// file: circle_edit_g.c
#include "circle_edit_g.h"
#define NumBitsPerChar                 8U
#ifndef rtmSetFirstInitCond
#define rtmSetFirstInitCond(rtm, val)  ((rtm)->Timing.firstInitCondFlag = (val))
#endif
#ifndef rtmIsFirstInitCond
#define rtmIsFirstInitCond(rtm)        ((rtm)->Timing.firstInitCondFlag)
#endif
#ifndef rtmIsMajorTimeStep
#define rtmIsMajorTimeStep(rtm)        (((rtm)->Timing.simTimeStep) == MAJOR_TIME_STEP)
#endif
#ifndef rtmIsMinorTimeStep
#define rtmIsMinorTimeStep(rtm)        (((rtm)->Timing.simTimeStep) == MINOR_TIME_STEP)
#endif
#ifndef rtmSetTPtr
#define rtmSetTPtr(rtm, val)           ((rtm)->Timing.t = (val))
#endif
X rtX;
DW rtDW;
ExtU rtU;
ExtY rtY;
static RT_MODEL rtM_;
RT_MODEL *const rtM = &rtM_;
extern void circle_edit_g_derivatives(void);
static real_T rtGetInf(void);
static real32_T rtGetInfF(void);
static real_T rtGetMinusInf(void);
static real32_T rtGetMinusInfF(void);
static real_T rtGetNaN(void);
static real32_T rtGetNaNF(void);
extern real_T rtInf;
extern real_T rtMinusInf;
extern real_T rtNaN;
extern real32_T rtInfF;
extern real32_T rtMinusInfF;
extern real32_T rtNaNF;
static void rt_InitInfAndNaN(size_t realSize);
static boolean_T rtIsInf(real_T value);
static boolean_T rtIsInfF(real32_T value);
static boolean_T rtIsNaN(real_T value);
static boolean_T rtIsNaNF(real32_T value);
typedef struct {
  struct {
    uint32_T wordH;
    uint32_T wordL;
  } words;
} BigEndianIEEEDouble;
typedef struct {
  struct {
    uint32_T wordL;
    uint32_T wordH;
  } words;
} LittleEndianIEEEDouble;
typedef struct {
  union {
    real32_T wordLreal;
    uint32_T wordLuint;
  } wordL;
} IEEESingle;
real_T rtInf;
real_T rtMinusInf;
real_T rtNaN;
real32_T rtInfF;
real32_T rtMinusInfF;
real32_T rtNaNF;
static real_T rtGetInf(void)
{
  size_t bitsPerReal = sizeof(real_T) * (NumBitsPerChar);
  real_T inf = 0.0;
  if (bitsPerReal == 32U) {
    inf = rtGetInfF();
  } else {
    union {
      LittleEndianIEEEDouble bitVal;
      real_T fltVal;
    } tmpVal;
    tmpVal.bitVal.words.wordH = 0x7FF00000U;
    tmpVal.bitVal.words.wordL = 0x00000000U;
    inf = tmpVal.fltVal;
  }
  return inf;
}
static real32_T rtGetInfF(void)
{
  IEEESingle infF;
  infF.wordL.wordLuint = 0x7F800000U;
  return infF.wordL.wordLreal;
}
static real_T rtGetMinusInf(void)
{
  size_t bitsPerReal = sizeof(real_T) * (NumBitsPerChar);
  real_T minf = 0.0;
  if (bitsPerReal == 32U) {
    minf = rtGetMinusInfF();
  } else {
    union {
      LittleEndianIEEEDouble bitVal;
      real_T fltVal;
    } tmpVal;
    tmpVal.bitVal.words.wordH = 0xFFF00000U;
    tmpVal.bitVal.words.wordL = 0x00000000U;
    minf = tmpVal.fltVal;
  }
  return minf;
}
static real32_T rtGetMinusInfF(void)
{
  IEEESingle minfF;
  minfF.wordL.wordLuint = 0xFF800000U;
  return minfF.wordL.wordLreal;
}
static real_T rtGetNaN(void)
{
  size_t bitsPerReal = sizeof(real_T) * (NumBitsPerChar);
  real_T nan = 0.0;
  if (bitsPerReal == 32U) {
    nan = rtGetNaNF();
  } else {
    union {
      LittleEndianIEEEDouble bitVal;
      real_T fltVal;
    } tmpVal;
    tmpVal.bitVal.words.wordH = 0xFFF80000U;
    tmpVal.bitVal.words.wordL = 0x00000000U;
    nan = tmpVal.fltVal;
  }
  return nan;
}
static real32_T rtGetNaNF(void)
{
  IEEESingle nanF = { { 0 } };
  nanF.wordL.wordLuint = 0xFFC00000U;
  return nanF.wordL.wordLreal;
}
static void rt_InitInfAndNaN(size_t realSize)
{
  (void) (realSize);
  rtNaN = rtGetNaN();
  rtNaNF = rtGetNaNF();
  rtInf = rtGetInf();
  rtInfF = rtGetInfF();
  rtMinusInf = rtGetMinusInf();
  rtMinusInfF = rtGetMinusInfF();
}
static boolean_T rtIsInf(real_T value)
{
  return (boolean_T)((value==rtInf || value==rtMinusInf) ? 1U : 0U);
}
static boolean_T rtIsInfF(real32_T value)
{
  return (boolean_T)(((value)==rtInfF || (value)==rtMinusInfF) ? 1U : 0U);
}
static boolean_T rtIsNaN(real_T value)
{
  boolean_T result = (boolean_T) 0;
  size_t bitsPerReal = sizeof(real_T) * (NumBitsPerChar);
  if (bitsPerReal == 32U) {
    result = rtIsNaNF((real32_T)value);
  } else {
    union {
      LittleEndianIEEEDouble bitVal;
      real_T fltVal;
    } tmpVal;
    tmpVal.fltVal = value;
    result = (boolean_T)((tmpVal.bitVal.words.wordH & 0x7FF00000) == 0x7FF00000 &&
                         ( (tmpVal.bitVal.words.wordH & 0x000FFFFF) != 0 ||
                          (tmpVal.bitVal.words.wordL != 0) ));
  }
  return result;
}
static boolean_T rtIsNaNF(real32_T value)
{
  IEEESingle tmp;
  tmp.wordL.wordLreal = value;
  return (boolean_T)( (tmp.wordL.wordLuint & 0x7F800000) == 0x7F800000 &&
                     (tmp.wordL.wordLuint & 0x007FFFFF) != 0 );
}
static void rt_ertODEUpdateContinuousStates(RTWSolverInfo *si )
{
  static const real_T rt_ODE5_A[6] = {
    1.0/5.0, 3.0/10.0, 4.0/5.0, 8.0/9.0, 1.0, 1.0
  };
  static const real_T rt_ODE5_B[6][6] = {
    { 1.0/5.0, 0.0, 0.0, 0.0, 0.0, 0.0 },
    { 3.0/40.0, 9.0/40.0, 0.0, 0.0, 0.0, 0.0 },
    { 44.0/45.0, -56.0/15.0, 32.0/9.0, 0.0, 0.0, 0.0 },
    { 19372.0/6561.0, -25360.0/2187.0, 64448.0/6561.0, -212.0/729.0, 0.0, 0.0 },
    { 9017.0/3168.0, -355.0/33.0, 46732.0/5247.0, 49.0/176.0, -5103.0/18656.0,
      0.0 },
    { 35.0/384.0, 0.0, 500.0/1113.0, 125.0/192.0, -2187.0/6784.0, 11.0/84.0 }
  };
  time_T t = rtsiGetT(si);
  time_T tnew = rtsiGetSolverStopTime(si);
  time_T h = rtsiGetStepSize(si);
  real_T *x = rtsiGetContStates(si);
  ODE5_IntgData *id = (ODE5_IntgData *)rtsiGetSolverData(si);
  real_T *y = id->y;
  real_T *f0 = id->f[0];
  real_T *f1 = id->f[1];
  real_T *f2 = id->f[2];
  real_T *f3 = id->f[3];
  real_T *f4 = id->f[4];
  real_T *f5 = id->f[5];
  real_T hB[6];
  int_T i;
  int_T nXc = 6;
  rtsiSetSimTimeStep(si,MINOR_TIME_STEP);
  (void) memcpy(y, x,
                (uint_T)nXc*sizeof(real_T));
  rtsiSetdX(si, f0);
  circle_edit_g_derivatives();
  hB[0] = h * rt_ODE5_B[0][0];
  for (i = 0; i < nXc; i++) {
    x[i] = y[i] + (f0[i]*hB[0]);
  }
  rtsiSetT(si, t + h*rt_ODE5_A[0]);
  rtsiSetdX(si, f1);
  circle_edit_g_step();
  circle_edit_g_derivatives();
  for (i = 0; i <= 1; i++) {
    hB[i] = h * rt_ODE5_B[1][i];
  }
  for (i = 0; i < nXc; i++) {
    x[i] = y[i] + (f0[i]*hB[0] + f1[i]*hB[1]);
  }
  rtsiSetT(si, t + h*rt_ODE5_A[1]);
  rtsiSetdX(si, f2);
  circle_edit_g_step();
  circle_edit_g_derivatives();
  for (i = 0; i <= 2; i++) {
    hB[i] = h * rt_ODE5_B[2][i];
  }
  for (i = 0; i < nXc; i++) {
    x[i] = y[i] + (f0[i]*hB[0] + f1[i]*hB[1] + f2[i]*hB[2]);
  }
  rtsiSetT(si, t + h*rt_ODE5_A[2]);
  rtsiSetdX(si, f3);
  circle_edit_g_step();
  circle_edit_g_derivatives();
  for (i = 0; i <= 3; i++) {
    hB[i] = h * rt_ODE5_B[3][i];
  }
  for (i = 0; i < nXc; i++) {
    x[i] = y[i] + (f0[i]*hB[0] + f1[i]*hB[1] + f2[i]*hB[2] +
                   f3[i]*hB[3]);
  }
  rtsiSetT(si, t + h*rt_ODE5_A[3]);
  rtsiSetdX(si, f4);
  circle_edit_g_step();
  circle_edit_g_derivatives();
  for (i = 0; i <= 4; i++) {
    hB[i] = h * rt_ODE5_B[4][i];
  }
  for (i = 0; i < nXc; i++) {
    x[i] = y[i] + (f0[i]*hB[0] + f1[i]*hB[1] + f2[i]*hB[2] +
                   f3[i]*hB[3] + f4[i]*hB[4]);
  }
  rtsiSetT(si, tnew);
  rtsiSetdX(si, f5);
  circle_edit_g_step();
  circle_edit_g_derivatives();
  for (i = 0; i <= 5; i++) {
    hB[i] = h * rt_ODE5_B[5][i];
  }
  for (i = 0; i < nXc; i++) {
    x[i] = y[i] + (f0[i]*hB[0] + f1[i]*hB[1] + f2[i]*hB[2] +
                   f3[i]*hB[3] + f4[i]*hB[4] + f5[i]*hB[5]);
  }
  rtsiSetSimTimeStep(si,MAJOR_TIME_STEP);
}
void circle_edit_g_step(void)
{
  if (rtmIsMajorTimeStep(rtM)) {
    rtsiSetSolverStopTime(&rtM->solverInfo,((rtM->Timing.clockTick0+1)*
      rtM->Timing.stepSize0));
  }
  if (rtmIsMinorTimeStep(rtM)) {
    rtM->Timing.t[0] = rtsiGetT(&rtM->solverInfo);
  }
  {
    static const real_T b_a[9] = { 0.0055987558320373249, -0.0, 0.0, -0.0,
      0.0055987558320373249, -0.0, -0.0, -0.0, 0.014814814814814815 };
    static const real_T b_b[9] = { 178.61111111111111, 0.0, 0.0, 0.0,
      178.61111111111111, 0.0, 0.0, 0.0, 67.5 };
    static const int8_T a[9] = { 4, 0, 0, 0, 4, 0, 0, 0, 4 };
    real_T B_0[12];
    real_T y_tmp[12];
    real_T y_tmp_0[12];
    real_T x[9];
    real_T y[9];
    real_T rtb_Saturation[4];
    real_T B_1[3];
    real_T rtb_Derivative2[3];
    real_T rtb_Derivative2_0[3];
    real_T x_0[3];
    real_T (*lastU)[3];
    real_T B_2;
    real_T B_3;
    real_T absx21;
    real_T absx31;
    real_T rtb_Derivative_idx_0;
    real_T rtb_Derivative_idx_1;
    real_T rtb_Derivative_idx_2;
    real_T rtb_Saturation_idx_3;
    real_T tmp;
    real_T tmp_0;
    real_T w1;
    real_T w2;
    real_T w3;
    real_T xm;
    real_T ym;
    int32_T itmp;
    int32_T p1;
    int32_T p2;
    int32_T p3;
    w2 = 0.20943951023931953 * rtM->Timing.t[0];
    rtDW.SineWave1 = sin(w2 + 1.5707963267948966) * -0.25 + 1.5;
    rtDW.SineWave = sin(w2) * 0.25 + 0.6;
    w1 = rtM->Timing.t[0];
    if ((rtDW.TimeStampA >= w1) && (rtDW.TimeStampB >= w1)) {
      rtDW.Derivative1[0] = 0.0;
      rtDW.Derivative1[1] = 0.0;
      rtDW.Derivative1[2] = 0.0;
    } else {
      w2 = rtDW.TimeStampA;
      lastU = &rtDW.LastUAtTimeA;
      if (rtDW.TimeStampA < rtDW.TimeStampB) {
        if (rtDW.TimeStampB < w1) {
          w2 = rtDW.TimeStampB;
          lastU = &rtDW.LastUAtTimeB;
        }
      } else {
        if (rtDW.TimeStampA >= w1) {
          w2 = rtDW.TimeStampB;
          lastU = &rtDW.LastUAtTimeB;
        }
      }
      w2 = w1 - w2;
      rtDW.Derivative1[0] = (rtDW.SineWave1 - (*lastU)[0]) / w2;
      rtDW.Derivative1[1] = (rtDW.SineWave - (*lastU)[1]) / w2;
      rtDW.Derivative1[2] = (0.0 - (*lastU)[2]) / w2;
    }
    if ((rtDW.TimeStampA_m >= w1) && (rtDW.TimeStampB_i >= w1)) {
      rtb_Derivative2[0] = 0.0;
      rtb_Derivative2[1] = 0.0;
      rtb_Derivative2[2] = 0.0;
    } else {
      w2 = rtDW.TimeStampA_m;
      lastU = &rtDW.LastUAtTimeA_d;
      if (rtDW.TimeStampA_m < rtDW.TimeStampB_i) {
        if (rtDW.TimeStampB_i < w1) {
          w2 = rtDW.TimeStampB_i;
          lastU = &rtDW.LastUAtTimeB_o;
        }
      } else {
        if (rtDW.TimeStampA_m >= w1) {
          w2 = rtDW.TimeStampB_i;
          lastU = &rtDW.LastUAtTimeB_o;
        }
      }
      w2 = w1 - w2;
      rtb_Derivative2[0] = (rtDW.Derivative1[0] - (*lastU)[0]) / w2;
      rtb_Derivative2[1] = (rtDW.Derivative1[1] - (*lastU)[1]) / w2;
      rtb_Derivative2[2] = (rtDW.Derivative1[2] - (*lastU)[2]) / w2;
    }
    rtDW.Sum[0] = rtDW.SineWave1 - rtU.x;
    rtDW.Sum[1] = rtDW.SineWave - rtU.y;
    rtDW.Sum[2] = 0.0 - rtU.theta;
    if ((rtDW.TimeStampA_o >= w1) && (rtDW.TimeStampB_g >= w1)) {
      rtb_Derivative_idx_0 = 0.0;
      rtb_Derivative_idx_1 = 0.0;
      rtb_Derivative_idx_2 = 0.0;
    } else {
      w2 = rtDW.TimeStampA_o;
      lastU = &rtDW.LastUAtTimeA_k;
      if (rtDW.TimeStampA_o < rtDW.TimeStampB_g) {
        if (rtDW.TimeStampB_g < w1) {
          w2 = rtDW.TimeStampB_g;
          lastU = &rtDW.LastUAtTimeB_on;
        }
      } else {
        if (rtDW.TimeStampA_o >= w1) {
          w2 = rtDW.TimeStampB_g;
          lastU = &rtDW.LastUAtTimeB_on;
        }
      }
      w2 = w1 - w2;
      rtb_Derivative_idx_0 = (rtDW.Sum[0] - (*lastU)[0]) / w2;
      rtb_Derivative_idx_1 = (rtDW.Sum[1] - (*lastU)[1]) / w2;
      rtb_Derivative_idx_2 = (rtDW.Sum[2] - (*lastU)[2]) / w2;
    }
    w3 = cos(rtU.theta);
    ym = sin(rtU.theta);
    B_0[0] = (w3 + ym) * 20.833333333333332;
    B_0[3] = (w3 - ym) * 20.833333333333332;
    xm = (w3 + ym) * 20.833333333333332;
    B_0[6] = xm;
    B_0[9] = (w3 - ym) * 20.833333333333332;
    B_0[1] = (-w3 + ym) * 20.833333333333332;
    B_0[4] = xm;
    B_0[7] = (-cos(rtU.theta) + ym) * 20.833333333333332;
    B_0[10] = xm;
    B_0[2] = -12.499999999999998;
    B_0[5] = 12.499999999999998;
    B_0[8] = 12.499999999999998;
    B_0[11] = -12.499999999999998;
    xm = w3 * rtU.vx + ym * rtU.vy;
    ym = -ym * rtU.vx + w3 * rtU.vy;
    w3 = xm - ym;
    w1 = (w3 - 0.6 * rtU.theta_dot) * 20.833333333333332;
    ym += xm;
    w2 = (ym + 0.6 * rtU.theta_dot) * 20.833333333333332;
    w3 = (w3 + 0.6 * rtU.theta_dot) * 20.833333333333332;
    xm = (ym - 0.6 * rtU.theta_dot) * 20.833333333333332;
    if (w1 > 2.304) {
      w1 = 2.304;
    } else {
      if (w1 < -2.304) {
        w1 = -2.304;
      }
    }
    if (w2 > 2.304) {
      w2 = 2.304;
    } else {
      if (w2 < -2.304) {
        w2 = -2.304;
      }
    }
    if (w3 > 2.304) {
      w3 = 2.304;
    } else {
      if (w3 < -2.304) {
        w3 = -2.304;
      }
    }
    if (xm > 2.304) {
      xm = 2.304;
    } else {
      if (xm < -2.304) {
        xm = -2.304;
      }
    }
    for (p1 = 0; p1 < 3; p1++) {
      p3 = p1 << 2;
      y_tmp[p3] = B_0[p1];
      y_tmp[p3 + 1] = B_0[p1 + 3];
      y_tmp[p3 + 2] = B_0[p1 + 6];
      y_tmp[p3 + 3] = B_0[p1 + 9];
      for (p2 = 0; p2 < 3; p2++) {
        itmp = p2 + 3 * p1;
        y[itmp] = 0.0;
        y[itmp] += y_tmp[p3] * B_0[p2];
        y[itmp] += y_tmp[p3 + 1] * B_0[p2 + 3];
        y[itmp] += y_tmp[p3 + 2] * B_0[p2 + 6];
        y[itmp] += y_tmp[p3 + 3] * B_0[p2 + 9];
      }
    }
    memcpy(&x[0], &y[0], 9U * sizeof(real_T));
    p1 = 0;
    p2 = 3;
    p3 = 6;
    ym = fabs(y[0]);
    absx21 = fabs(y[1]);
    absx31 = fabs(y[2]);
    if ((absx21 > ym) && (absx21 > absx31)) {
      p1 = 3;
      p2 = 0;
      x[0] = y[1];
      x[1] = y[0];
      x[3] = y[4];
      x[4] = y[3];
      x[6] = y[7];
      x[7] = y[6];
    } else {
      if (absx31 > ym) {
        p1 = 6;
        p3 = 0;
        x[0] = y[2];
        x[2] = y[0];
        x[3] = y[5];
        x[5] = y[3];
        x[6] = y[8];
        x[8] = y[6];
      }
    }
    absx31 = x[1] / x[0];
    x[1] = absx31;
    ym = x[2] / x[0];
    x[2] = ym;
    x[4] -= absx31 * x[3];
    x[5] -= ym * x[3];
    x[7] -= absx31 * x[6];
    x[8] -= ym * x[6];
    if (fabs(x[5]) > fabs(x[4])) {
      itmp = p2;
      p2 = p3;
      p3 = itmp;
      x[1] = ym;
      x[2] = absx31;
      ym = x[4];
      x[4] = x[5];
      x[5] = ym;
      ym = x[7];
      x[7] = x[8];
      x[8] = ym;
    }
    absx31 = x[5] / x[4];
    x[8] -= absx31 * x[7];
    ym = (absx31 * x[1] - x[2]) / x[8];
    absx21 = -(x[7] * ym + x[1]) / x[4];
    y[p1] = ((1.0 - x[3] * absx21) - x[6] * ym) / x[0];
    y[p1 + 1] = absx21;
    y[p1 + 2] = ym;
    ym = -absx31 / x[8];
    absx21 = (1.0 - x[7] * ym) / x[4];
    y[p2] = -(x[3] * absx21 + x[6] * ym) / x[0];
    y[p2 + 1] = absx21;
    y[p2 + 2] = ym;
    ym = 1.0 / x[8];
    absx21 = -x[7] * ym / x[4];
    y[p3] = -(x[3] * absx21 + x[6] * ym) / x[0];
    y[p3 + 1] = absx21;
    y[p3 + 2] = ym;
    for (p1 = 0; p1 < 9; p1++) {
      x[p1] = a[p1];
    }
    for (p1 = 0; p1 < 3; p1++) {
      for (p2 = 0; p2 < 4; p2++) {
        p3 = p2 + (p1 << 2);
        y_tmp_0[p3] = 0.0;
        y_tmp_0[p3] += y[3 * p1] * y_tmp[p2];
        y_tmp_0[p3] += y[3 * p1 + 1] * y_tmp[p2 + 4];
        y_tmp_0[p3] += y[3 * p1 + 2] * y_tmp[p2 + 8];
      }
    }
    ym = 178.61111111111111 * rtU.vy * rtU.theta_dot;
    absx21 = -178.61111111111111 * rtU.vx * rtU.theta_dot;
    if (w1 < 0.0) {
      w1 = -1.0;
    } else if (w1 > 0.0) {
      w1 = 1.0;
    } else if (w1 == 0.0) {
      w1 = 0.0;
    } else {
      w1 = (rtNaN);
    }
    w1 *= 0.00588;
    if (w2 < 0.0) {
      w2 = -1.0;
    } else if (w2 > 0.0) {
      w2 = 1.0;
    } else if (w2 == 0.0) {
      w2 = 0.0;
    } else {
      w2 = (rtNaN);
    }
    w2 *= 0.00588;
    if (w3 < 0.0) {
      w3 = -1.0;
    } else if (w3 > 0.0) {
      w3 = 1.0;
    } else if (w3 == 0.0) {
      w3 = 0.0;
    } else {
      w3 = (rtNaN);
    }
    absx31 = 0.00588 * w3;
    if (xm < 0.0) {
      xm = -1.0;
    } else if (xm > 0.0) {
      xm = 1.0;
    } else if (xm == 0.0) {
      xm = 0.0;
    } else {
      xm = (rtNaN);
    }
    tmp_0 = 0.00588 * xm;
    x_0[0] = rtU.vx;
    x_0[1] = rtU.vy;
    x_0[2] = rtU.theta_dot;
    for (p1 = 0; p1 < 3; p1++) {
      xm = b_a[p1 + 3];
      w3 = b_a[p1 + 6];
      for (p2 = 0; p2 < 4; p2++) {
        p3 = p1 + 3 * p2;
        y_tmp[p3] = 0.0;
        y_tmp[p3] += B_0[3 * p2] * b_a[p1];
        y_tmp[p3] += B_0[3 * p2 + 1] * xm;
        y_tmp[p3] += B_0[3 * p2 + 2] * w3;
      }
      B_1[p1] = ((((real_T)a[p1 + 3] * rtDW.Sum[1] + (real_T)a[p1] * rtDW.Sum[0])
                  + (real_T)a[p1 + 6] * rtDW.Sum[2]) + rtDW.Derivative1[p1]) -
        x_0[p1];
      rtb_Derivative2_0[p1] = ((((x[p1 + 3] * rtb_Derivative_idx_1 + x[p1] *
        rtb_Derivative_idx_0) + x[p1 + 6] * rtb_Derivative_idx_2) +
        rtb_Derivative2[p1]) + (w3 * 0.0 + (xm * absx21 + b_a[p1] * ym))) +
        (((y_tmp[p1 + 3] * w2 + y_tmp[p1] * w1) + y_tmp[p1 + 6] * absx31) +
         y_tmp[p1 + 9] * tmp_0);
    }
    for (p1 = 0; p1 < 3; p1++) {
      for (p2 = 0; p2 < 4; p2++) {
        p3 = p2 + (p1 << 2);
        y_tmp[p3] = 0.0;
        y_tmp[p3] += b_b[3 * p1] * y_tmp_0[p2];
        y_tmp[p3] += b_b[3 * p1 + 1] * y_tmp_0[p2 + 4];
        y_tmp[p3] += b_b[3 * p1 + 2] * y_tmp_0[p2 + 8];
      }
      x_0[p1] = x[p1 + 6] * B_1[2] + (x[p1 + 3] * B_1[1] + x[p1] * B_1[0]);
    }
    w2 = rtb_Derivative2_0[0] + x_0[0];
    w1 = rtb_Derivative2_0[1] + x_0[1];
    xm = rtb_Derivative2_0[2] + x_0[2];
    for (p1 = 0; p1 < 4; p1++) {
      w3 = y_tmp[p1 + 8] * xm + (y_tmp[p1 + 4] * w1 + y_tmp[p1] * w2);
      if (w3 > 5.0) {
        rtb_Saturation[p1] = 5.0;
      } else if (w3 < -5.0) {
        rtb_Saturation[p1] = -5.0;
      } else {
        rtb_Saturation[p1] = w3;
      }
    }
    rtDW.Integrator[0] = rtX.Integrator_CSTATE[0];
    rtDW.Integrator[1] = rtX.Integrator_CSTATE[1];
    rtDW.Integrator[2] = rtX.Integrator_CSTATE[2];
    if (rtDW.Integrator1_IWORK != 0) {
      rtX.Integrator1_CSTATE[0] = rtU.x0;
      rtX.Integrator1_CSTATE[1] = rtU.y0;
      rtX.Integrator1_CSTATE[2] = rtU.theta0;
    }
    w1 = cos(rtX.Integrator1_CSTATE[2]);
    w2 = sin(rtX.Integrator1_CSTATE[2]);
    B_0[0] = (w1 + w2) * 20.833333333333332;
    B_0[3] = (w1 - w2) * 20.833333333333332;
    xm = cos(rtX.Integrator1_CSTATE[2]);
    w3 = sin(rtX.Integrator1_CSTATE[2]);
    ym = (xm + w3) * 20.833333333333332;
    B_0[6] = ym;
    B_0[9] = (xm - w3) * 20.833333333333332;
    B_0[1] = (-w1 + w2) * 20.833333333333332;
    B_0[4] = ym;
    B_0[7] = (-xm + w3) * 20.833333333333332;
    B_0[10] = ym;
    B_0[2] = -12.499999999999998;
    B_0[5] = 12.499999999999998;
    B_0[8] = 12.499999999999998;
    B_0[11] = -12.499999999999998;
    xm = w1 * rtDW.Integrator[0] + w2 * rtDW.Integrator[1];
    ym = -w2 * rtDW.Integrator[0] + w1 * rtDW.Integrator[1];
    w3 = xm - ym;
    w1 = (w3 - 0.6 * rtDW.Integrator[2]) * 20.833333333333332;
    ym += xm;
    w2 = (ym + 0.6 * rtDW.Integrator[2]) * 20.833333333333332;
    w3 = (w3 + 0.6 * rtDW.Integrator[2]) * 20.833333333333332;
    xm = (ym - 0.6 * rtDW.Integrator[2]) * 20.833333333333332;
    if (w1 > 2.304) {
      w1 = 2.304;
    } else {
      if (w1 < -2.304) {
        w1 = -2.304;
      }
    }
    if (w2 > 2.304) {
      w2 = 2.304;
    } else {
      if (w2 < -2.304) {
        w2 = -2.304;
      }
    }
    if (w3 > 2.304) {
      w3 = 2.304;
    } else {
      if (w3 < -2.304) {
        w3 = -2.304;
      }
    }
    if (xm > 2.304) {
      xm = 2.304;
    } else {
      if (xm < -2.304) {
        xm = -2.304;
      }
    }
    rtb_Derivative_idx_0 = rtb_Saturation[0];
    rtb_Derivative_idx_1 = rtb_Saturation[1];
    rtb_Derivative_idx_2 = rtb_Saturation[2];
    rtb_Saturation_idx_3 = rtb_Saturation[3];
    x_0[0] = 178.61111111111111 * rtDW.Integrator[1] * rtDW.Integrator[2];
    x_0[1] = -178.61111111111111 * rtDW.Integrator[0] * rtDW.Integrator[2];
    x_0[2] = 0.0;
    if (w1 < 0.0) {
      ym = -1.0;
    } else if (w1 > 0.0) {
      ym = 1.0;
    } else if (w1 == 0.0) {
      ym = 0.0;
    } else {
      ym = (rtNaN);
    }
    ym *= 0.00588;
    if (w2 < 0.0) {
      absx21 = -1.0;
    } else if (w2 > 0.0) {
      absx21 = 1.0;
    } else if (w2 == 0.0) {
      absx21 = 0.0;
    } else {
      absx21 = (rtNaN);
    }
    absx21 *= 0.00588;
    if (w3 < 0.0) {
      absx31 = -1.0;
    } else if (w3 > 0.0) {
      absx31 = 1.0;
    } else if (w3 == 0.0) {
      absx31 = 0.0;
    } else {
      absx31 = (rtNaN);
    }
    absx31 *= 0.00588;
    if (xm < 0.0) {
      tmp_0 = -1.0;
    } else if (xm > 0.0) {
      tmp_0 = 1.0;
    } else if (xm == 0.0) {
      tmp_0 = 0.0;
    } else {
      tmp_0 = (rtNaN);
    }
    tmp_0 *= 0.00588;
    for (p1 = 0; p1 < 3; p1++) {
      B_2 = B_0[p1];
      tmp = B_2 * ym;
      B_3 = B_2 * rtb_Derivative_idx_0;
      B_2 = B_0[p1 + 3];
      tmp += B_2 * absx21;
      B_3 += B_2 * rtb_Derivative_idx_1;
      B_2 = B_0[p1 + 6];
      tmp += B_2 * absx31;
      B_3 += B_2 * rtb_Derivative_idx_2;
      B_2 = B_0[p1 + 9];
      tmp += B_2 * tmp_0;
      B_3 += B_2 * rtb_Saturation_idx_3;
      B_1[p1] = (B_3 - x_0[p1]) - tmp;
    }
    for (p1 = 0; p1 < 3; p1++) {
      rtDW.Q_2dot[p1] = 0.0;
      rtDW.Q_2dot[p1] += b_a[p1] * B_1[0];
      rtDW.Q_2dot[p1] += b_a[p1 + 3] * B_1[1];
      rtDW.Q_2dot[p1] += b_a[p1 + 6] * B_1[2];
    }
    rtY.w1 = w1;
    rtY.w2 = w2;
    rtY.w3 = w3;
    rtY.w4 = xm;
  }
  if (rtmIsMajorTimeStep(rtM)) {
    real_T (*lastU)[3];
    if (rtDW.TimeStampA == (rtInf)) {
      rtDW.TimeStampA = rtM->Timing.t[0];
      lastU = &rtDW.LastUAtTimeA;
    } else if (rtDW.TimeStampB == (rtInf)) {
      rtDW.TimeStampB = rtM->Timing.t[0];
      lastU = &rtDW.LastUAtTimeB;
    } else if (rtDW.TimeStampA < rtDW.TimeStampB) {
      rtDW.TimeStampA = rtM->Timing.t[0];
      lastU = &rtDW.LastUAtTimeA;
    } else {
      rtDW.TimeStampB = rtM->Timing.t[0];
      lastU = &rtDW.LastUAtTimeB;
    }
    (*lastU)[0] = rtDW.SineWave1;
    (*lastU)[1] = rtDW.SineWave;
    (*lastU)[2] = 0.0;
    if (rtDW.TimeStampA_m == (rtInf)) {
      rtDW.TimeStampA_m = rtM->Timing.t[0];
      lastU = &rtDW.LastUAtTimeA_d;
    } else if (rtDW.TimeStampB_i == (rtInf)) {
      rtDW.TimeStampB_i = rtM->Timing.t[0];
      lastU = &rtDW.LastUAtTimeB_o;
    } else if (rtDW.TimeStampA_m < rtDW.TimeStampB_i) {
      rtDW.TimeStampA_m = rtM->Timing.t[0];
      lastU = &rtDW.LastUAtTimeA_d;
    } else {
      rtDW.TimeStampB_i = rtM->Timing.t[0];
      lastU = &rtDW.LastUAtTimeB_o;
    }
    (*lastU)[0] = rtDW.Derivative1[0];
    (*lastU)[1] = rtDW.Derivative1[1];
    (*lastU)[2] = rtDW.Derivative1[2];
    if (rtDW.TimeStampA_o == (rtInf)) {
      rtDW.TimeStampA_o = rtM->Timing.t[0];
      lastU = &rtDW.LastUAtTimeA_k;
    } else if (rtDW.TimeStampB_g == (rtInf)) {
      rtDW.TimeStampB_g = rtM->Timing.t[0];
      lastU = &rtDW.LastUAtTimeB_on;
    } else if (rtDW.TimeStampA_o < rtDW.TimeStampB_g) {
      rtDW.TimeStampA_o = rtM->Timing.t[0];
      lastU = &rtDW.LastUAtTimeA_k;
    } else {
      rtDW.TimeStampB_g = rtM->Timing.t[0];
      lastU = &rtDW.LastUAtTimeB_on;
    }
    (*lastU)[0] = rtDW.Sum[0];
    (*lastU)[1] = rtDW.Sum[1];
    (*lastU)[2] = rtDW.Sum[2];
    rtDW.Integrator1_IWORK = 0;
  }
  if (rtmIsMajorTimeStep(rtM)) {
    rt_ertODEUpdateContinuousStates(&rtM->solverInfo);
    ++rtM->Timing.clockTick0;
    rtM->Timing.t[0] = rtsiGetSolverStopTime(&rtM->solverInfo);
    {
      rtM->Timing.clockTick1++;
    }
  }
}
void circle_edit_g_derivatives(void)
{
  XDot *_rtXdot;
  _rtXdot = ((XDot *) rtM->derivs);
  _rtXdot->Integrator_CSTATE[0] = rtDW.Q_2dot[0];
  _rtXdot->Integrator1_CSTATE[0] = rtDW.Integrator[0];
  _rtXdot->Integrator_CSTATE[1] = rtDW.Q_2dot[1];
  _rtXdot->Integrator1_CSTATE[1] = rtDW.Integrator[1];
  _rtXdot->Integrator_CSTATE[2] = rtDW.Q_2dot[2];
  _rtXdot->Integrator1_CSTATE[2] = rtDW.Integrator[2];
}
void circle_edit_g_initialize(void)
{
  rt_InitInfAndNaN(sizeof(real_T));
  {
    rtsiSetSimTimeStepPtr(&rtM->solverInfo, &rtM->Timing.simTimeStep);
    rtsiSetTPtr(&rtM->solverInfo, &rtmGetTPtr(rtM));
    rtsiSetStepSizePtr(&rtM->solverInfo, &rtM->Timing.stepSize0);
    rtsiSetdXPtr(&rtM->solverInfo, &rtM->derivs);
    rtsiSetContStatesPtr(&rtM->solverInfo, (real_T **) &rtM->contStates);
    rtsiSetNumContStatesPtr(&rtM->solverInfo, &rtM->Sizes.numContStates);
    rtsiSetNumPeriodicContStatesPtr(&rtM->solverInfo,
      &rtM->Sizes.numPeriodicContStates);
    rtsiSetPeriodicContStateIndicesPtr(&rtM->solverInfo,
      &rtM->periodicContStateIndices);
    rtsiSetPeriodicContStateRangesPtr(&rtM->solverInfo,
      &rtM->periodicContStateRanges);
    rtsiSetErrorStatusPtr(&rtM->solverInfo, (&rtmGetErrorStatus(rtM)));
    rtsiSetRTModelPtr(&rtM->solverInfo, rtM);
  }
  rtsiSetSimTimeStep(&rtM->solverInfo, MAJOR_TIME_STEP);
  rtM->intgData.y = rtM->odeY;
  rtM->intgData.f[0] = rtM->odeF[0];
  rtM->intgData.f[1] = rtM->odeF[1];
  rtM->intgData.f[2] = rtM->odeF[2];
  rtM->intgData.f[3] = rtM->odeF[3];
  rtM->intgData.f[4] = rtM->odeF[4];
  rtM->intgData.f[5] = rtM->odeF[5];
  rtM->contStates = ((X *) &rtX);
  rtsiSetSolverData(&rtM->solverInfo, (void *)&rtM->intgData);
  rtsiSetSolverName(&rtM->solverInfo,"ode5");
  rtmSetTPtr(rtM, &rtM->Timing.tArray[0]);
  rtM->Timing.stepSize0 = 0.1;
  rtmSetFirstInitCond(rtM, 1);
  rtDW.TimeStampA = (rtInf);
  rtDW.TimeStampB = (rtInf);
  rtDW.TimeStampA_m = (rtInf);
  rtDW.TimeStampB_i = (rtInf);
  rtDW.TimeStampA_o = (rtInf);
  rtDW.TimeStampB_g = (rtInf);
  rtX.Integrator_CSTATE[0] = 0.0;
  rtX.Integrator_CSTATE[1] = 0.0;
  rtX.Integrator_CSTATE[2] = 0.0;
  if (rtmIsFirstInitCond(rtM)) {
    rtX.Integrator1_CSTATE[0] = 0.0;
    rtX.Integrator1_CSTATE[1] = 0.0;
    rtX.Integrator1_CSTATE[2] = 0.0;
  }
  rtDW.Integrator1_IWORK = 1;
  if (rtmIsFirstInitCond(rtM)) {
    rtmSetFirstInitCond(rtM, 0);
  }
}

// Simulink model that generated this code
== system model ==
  Inport#1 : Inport
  Inport#2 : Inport
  theta : Inport
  vx : Inport
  vy : Inport
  theta_dot : Inport
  x0 : Inport
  y0 : Inport
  theta0 : Inport
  w1 : Outport  <- 1: MATLABFunction#1/2
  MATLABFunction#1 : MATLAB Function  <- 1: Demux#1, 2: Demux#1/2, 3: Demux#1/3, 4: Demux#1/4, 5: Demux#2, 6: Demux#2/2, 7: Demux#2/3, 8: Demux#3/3
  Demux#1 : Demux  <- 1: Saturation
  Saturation : Saturate  UpperLimit=5  LowerLimit=-5  <- 1: MATLABFunction#2
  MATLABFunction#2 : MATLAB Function  <- 1: Derivative2, 2: Derivative, 3: MATLABFunction#3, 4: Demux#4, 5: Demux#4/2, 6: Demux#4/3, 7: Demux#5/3
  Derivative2 : Derivative  <- 1: Derivative1
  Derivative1 : Derivative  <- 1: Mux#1
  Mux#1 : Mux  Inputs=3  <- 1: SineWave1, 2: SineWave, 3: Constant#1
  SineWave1 : Sin  Amplitude=-0.25  Bias=1.5  Frequency=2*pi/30  Phase=pi/2
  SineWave : Sin  Amplitude=0.25  Bias=0.6  Frequency=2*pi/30
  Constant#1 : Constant  Value=0
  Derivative : Derivative  <- 1: Sum
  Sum : Sum  Inputs=+-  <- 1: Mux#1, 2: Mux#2
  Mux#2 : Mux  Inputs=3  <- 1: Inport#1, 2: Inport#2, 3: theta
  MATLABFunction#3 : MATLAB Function  <- 1: Derivative1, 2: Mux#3, 3: Sum
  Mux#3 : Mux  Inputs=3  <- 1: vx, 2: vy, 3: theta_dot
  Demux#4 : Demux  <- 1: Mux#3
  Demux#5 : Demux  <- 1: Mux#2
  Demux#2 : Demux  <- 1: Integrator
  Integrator : Integrator  <- 1: MATLABFunction#1
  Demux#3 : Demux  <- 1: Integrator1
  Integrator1 : Integrator  InitialCondition=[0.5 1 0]  <- 1: Integrator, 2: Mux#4
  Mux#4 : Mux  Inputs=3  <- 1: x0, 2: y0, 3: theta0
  w2 : Outport  <- 1: MATLABFunction#1/3
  w3 : Outport  <- 1: MATLABFunction#1/4
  w4 : Outport  <- 1: MATLABFunction#1/5
== matlab function MATLABFunction#1 ==
function [Q_2dot,w1,w2,w3,w4]  = fcn(T1, T2, T3, T4,x_dot,y_dot,theta_dot,theta)

m=5;
I=5;
Ib=0.1;
l1= 0.3;
l2=0.3;
r=0.048;
g=9.8;
u=0.01;
N = m*g/4;
M=[(m+4*Ib/(r*r)) 0 0; 0 (m+4*Ib/(r*r)) 0; 0 0 (I+4*Ib*(l1+l2)*(l1+l2)/(r*r))];
C= [(m+4*Ib/(r*r))*y_dot*theta_dot;-(m+4*Ib/(r*r))*x_dot*theta_dot;0 ];
B=(1/r)*[(cos(theta)+sin(theta)) (cos(theta)-sin(theta)) (cos(theta)+sin(theta)) (cos(theta)-sin(theta));
         (-cos(theta)+sin(theta)) (cos(theta)+sin(theta)) (-cos(theta)+sin(theta)) (cos(theta)+sin(theta)); 
         (-(l1+l2)) (l1+l2) (l1+l2) (-(l1+l2)) ];
T=[T1;T2;T3;T4];
xm= cos(theta)*x_dot+sin(theta)*y_dot;
ym= -sin(theta)*x_dot+cos(theta)*y_dot;
w1 = (1/r)*(xm-ym-(l1+l2)*theta_dot);
w2 = (1/r)*(xm+ym+(l1+l2)*theta_dot);
w3 = (1/r)*(xm-ym+(l1+l2)*theta_dot);
w4 = (1/r)*(xm+ym-(l1+l2)*theta_dot);
w_max = 2.304;
if w1 > w_max
    w1 = w_max; %w = 20.83
elseif w1 < -w_max
    w1 = -w_max;
end
if w2 > w_max
    w2 = w_max;
elseif w2 < -w_max
    w2 = -w_max;
end
if w3 > w_max
    w3 = w_max;
elseif w3 < -w_max
    w3 = -w_max;
end
if w4 > w_max
    w4 = w_max;
elseif w4 < -w_max
    w4 = -w_max;
end
Xi=[u*r*N*sign(w1);u*r*N*sign(w2);u*r*N*sign(w3);u*N*r*sign(w4)];

Q_2dot=inv(M)*(B*T-C-B*Xi);

== matlab function MATLABFunction#2 ==
function u_control = fcn(Qr_2dot,e1_dot,e2,x_dot,y_dot,theta_dot,theta)

m=5;
I=5;
Ib=0.1;
l1= 0.3;
l2=0.3;
r=0.048;
g=9.8;
u=0.01;
N = m*g/4;
M=[(m+4*Ib/(r*r)) 0 0; 0 (m+4*Ib/(r*r)) 0; 0 0 (I+4*Ib*(l1+l2)*(l1+l2)/(r*r))];
C= [(m+4*Ib/(r*r))*y_dot*theta_dot;-(m+4*Ib/(r*r))*x_dot*theta_dot;0 ];
B=(1/r)*[(cos(theta)+sin(theta)) (cos(theta)-sin(theta)) (cos(theta)+sin(theta)) (cos(theta)-sin(theta));
    (-cos(theta)+sin(theta)) (cos(theta)+sin(theta)) (-cos(theta)+sin(theta)) (cos(theta)+sin(theta)); 
    (-(l1+l2)) (l1+l2) (l1+l2) (-(l1+l2)) ];

xm= cos(theta)*x_dot+sin(theta)*y_dot;
ym= -sin(theta)*x_dot+cos(theta)*y_dot;
w1 = (1/r)*(xm-ym-(l1+l2)*theta_dot);
w2 = (1/r)*(xm+ym+(l1+l2)*theta_dot);
w3 = (1/r)*(xm-ym+(l1+l2)*theta_dot);
w4 = (1/r)*(xm+ym-(l1+l2)*theta_dot);
w_max = 2.304;
if w1 > w_max
    w1 = w_max; %w = 20.83
elseif w1 < -w_max
    w1 = -w_max;
end
if w2 > w_max
    w2 = w_max;
elseif w2 < -w_max
    w2 = -w_max;
end
if w3 > w_max
    w3 = w_max;
elseif w3 < -w_max
    w3 = -w_max;
end
if w4 > w_max
    w4 = w_max;
elseif w4 < -w_max
    w4 = -w_max;
end
Xi=[u*r*N*sign(w1);u*r*N*sign(w2);u*r*N*sign(w3);u*N*r*sign(w4)];

k1 = [4 0 0;
      0 4 0;
      0 0 4];
k2 = [4 0 0;
      0 4 0;
      0 0 4];
  
u_control = B'*inv(B*B')*M*((Qr_2dot+k1*e1_dot)+inv(M)*C+inv(M)*B*Xi+k2*e2);

== matlab function MATLABFunction#3 ==
function e2  = fcn(Qr_dot,Q_dot,e1)

k1 = [4 0 0;
      0 4 0;
      0 0 4];
 
%x2r_dot = (Qr_2dot+k1*e1_dot);
x2r = Qr_dot + k1*e1;
e2 = x2r - Q_dot;
